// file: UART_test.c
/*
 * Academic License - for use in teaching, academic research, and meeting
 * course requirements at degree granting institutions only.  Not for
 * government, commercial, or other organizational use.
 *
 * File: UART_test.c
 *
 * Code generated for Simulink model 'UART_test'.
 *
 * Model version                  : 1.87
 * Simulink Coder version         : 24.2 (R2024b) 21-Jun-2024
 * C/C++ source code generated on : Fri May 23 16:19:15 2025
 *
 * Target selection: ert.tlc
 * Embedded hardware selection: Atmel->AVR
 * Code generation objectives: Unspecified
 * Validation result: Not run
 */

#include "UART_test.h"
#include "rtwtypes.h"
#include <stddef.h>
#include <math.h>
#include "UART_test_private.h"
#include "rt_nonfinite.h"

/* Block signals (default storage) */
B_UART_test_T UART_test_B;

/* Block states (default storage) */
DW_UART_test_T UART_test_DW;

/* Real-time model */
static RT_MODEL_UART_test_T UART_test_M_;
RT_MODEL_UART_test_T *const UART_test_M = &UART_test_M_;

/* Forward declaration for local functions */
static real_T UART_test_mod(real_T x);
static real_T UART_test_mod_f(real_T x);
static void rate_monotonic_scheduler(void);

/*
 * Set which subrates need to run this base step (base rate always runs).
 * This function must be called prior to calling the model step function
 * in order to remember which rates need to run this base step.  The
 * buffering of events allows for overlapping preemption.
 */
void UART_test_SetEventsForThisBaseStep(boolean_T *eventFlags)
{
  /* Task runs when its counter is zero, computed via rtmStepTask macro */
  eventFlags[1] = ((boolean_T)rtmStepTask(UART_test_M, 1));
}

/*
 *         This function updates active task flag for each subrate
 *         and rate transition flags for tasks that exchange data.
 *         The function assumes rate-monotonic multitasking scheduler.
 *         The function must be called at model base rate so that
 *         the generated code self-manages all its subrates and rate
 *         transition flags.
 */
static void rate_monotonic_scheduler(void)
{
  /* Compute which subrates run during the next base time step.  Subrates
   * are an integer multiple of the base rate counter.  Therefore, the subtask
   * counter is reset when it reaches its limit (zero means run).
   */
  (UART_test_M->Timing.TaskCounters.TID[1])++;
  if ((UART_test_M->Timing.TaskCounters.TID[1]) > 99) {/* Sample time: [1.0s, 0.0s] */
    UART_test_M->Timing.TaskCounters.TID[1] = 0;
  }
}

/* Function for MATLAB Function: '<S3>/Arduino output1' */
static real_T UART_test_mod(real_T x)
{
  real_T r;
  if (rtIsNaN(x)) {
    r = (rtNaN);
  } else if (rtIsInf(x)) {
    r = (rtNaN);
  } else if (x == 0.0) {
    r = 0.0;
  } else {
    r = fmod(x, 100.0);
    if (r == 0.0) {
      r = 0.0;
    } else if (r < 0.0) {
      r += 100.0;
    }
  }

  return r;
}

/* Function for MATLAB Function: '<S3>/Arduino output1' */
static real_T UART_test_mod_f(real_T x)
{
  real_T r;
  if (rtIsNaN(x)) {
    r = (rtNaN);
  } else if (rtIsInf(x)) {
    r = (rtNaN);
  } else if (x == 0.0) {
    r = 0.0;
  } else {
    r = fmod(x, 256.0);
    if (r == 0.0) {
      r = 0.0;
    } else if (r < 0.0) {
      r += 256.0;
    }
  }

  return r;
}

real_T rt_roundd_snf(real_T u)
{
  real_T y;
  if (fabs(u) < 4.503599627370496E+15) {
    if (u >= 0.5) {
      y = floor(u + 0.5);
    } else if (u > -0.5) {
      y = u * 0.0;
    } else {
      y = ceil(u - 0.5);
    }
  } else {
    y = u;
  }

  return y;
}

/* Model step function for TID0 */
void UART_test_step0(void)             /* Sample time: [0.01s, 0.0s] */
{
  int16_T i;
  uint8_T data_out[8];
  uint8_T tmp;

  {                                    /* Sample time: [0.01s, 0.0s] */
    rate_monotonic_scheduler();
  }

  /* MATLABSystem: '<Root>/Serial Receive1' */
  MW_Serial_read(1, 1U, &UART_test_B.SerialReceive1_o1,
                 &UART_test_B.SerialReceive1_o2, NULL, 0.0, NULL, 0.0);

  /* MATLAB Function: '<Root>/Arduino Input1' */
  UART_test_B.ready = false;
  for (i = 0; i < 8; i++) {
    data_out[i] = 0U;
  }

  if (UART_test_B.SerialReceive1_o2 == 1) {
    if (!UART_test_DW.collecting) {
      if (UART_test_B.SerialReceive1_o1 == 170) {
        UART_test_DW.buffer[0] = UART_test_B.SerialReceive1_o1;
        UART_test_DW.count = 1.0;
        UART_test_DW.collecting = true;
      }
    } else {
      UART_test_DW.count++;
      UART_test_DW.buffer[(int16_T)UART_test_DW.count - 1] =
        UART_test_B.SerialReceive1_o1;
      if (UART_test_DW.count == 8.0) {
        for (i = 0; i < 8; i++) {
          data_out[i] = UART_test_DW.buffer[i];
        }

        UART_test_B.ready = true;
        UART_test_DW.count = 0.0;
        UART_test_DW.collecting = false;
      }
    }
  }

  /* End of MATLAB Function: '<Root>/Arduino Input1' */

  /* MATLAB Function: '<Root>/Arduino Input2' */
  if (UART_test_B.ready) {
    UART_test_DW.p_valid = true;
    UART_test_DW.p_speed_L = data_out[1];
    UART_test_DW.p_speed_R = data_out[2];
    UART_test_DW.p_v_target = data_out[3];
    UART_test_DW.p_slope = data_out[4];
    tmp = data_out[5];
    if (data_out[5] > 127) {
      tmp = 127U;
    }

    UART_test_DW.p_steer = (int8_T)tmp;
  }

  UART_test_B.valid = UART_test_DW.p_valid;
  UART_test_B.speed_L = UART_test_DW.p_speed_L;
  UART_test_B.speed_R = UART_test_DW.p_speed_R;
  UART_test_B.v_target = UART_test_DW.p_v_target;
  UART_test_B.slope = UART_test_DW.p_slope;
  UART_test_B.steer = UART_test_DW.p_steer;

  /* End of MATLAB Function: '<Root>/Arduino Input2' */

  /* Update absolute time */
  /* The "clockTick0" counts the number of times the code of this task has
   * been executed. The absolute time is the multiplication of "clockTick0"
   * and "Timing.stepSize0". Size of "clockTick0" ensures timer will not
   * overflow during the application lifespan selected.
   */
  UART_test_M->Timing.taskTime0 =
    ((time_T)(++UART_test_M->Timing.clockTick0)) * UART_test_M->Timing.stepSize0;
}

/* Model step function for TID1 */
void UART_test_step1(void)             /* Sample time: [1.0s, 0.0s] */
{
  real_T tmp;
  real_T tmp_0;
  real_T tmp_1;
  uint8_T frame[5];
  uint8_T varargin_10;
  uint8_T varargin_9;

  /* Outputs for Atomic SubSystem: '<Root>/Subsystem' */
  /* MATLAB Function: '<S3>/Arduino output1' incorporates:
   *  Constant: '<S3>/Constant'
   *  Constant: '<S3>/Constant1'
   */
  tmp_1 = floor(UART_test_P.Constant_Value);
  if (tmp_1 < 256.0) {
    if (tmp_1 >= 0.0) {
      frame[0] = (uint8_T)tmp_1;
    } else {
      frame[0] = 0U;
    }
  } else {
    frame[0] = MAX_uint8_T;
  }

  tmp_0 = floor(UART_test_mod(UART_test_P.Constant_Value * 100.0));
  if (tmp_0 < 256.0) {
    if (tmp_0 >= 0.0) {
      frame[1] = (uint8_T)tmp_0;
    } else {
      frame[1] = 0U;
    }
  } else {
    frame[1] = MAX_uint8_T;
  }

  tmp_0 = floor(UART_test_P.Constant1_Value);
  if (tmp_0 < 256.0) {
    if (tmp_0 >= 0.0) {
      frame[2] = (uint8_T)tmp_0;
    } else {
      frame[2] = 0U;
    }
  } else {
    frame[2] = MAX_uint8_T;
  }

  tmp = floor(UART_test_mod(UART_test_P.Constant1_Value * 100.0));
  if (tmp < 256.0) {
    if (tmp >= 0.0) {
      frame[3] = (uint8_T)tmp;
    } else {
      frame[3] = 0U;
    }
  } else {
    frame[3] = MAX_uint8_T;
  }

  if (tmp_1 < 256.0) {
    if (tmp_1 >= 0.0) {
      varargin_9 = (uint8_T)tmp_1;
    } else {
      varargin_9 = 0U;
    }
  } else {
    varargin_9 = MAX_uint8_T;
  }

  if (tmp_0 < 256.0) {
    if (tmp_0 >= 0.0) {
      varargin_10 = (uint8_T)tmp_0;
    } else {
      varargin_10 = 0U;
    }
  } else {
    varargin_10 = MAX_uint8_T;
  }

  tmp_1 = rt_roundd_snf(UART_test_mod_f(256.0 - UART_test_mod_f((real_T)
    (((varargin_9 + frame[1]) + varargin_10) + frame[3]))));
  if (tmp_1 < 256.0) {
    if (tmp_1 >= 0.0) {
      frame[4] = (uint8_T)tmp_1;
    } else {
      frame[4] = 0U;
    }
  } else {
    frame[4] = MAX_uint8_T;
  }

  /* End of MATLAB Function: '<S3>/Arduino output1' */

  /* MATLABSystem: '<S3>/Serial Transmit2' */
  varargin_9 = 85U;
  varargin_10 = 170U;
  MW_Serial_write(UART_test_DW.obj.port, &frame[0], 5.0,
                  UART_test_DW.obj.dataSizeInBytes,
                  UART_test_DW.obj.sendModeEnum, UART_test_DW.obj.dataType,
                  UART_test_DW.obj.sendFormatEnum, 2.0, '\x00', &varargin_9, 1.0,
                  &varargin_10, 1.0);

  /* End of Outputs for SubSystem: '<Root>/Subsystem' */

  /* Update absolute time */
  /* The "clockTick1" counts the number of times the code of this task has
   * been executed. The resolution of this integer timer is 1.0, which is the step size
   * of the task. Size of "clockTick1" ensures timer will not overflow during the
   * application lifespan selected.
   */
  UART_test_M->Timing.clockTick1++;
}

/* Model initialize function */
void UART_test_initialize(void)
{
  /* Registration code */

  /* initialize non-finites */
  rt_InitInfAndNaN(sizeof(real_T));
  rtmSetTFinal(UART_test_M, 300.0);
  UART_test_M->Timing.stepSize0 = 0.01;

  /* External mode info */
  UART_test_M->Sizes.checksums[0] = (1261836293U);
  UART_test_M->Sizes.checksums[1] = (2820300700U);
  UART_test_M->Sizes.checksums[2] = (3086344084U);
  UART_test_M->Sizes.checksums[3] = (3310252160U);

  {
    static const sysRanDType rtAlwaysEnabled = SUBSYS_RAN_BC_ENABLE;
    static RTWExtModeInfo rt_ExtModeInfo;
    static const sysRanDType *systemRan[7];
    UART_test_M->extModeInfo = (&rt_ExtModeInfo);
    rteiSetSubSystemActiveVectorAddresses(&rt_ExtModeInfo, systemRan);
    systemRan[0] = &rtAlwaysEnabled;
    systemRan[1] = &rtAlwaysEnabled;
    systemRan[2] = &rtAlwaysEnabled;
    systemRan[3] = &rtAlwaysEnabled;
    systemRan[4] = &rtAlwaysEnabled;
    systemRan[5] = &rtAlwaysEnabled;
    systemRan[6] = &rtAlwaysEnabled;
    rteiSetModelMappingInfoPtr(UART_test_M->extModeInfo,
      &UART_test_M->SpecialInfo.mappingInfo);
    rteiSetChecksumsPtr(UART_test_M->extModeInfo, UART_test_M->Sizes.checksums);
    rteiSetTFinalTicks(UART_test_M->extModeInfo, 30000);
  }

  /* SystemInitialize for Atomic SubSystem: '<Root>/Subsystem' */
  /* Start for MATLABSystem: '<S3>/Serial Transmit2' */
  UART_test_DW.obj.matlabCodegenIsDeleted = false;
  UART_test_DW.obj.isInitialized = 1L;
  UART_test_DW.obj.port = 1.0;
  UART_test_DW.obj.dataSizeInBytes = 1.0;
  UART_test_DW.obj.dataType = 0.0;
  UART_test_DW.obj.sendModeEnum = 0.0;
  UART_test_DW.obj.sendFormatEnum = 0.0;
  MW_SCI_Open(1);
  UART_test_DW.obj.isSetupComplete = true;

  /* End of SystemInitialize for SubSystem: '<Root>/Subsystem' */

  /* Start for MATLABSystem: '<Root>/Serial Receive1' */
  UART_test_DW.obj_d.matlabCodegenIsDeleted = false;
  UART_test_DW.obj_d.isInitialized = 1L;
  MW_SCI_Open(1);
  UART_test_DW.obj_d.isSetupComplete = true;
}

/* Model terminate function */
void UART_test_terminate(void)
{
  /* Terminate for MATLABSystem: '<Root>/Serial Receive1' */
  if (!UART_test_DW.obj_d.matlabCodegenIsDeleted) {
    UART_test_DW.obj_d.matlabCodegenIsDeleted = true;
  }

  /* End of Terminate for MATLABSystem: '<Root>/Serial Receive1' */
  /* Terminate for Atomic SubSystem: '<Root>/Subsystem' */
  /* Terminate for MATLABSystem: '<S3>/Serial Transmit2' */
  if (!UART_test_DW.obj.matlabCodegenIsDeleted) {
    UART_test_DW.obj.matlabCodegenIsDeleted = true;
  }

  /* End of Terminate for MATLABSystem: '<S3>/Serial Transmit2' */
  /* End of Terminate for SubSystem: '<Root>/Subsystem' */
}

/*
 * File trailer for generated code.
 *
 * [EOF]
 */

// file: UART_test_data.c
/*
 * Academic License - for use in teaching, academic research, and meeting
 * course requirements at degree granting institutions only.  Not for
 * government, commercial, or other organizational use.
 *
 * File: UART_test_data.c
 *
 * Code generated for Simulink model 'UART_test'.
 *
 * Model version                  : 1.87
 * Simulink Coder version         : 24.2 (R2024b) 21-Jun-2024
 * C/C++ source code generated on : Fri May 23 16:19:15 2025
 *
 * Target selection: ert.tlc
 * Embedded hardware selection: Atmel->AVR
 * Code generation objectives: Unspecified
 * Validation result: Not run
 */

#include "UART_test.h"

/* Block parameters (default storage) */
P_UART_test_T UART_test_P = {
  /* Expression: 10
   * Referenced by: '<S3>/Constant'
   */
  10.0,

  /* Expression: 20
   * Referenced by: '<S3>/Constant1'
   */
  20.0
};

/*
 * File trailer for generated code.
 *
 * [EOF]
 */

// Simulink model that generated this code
simulink model "UART_test"  (R2024b)
settings: Solver=FixedStepAuto  StartTime=0.0  StopTime=300  FixedStep=0.01  RelTol=1e-3  EnableMultiTasking=on
libraries: arduinolib x2

== system UART_test ==
  Arduino Input1 : MATLAB Function  TreatAsAtomicUnit=on
  Arduino Input2 : MATLAB Function  TreatAsAtomicUnit=on
  Display{,1..5,7} (7 alike) : Display
  S-Function : S-Function  Commented=on  FunctionName=sfun_uart  SFunctionDeploymentMode=off  EnableBusSupport=off
  Serial Receive1 : arduinolib/Serial Receive  portNumber=1  DataType=uint8  blockPlatform=ARDUINO  TimeOut=0  MaxDataLength=10  isARMArch=off  DataLengthOption=Length via dialog  Datalength=1  Header=[]  Terminator=[]  SampleTime=0.01  ShowOutStatus=on
  Subsystem : Subsystem  TreatAsAtomicUnit=on  SystemSampleTime=1
  valid : Display
  valid1 : Display
  wires:
  Arduino Input1/2(data_out) -> Arduino Input2/2(u)
  Arduino Input1/1(ready) -> valid/1, Arduino Input2/1(ready)
  Serial Receive1/1 -> valid1/1, Arduino Input1/1(byte_in)
  Serial Receive1/2 -> Display7/1, Arduino Input1/2(status)
  Arduino Input2/1(valid) -> Display/1
  Arduino Input2/2(speed_L) -> Display1/1
  Arduino Input2/3(speed_R) -> Display2/1
  Arduino Input2/4(v_target) -> Display3/1
  Arduino Input2/5(slope) -> Display4/1
  Arduino Input2/6(steer) -> Display5/1

== system UART_test/Subsystem ==
  Arduino output1 : MATLAB Function  TreatAsAtomicUnit=on
  Constant : Constant  Value=10
  Constant1 : Constant  Value=20
  Serial Transmit2 : arduinolib/Serial Transmit  portNumber=1  sendmode=write  sendformat=Decimal  floatprecision=2  header=[0xAA]  terminator=[0x55]  blockPlatform=ARDUINO
  wires:
  Constant1/1 -> Arduino output1/2(vR)
  Arduino output1/1(frame) -> Serial Transmit2/1
  Constant/1 -> Arduino output1/1(vL)

== matlab function UART_test/Arduino Input2 ==
function [valid, speed_L, speed_R, v_target, slope, steer] = parseUART_persistent(ready, u)
% UART 패킷 파서 (persistent 방식으로 이전 값 유지)
% u: [10x1] uint8, 패킷 데이터
% ready: 패킷 유효 신호

%#codegen

% 이전 출력값 저장용 persistent 변수
persistent p_valid p_speed_L p_speed_R p_v_target p_slope p_steer

% 초기화 (최초 실행 시)
if isempty(p_valid)
    p_valid = false;
    p_speed_L = 0.0;
    p_speed_R = 0.0;
    p_v_target = uint8(0);
    p_slope = uint8(0);
    p_steer = int8(0);
end

% 새로운 데이터가 들어왔을 경우만 업데이트
if ready == 1
        p_valid = true;
        p_speed_L = double(u(2));
        p_speed_R = double(u(3));
        p_v_target = u(4);
        p_slope = u(5);
        p_steer = int8(u(6));
end

% 항상 마지막 유효 출력 반환
valid     = p_valid;
speed_L   = p_speed_L;
speed_R   = p_speed_R;
v_target  = p_v_target;
slope     = p_slope;
steer     = p_steer;

== matlab function UART_test/Subsystem/Arduino output1 ==
function frame = makeFrame(vL, vR)
% 입력:
%   vL, vR : 좌/우 목표 속도 (실수, cm/s 단위)
% 출력:
%   frame : 7-byte UART 전송 프레임 (uint8 벡터)
    frame = zeros(5,1,'uint8');  % 7바이트 프레임

    % 2-3. 목표속도_L (정수 + 소수)
    frame(1) = uint8(floor(vL));                       % 정수부
    frame(2) = uint8(floor(mod(vL * 100, 100)));       % 소수부 (소수점 둘째 자리까지)

    % 4-5. 목표속도_R (정수 + 소수)
    frame(3) = uint8(floor(vR));                       % 정수부
    frame(4) = uint8(floor(mod(vR * 100, 100)));       % 소수부

    % 6. CRC: 256 - (sum of byte 1~5) % 256
    crc = mod(sum(double(frame(1:5))), 256);
    frame(5) = uint8(mod(256 - crc, 256));
    
end

== matlab function UART_test/Arduino Input1 ==
function [ready, data_out] = uart_parser(byte_in, status)
% UART 프레임 수신기 (Start Byte = 0xAA, Total = 10 bytes)
% 입력: byte_in - 1바이트씩 들어오는 uint8
% 입력: status - Serial Receive의 상태 (1이면 수신 성공)
% 출력: ready - 1이면 패킷 파싱 완료
% 출력: data_out - [1x10] uint8, 패킷 데이터

persistent buffer count collecting

if isempty(buffer)
    buffer = zeros(1, 8, 'uint8');
    count = 0;
    collecting = false;
end

ready = false;
data_out = zeros(1,8,'uint8');

if status == 1
    if ~collecting
        % 아직 수집 시작 전 → start byte 찾기
        if byte_in == hex2dec('AA')
            buffer(1) = byte_in;
            count = 1;
            collecting = true;
        end
    else
        % 수집 중
        count = count + 1;
        buffer(count) = byte_in;

        if count == 8
            data_out = buffer;
            ready = true;
            count = 0;
            collecting = false;
        end
    end
end
